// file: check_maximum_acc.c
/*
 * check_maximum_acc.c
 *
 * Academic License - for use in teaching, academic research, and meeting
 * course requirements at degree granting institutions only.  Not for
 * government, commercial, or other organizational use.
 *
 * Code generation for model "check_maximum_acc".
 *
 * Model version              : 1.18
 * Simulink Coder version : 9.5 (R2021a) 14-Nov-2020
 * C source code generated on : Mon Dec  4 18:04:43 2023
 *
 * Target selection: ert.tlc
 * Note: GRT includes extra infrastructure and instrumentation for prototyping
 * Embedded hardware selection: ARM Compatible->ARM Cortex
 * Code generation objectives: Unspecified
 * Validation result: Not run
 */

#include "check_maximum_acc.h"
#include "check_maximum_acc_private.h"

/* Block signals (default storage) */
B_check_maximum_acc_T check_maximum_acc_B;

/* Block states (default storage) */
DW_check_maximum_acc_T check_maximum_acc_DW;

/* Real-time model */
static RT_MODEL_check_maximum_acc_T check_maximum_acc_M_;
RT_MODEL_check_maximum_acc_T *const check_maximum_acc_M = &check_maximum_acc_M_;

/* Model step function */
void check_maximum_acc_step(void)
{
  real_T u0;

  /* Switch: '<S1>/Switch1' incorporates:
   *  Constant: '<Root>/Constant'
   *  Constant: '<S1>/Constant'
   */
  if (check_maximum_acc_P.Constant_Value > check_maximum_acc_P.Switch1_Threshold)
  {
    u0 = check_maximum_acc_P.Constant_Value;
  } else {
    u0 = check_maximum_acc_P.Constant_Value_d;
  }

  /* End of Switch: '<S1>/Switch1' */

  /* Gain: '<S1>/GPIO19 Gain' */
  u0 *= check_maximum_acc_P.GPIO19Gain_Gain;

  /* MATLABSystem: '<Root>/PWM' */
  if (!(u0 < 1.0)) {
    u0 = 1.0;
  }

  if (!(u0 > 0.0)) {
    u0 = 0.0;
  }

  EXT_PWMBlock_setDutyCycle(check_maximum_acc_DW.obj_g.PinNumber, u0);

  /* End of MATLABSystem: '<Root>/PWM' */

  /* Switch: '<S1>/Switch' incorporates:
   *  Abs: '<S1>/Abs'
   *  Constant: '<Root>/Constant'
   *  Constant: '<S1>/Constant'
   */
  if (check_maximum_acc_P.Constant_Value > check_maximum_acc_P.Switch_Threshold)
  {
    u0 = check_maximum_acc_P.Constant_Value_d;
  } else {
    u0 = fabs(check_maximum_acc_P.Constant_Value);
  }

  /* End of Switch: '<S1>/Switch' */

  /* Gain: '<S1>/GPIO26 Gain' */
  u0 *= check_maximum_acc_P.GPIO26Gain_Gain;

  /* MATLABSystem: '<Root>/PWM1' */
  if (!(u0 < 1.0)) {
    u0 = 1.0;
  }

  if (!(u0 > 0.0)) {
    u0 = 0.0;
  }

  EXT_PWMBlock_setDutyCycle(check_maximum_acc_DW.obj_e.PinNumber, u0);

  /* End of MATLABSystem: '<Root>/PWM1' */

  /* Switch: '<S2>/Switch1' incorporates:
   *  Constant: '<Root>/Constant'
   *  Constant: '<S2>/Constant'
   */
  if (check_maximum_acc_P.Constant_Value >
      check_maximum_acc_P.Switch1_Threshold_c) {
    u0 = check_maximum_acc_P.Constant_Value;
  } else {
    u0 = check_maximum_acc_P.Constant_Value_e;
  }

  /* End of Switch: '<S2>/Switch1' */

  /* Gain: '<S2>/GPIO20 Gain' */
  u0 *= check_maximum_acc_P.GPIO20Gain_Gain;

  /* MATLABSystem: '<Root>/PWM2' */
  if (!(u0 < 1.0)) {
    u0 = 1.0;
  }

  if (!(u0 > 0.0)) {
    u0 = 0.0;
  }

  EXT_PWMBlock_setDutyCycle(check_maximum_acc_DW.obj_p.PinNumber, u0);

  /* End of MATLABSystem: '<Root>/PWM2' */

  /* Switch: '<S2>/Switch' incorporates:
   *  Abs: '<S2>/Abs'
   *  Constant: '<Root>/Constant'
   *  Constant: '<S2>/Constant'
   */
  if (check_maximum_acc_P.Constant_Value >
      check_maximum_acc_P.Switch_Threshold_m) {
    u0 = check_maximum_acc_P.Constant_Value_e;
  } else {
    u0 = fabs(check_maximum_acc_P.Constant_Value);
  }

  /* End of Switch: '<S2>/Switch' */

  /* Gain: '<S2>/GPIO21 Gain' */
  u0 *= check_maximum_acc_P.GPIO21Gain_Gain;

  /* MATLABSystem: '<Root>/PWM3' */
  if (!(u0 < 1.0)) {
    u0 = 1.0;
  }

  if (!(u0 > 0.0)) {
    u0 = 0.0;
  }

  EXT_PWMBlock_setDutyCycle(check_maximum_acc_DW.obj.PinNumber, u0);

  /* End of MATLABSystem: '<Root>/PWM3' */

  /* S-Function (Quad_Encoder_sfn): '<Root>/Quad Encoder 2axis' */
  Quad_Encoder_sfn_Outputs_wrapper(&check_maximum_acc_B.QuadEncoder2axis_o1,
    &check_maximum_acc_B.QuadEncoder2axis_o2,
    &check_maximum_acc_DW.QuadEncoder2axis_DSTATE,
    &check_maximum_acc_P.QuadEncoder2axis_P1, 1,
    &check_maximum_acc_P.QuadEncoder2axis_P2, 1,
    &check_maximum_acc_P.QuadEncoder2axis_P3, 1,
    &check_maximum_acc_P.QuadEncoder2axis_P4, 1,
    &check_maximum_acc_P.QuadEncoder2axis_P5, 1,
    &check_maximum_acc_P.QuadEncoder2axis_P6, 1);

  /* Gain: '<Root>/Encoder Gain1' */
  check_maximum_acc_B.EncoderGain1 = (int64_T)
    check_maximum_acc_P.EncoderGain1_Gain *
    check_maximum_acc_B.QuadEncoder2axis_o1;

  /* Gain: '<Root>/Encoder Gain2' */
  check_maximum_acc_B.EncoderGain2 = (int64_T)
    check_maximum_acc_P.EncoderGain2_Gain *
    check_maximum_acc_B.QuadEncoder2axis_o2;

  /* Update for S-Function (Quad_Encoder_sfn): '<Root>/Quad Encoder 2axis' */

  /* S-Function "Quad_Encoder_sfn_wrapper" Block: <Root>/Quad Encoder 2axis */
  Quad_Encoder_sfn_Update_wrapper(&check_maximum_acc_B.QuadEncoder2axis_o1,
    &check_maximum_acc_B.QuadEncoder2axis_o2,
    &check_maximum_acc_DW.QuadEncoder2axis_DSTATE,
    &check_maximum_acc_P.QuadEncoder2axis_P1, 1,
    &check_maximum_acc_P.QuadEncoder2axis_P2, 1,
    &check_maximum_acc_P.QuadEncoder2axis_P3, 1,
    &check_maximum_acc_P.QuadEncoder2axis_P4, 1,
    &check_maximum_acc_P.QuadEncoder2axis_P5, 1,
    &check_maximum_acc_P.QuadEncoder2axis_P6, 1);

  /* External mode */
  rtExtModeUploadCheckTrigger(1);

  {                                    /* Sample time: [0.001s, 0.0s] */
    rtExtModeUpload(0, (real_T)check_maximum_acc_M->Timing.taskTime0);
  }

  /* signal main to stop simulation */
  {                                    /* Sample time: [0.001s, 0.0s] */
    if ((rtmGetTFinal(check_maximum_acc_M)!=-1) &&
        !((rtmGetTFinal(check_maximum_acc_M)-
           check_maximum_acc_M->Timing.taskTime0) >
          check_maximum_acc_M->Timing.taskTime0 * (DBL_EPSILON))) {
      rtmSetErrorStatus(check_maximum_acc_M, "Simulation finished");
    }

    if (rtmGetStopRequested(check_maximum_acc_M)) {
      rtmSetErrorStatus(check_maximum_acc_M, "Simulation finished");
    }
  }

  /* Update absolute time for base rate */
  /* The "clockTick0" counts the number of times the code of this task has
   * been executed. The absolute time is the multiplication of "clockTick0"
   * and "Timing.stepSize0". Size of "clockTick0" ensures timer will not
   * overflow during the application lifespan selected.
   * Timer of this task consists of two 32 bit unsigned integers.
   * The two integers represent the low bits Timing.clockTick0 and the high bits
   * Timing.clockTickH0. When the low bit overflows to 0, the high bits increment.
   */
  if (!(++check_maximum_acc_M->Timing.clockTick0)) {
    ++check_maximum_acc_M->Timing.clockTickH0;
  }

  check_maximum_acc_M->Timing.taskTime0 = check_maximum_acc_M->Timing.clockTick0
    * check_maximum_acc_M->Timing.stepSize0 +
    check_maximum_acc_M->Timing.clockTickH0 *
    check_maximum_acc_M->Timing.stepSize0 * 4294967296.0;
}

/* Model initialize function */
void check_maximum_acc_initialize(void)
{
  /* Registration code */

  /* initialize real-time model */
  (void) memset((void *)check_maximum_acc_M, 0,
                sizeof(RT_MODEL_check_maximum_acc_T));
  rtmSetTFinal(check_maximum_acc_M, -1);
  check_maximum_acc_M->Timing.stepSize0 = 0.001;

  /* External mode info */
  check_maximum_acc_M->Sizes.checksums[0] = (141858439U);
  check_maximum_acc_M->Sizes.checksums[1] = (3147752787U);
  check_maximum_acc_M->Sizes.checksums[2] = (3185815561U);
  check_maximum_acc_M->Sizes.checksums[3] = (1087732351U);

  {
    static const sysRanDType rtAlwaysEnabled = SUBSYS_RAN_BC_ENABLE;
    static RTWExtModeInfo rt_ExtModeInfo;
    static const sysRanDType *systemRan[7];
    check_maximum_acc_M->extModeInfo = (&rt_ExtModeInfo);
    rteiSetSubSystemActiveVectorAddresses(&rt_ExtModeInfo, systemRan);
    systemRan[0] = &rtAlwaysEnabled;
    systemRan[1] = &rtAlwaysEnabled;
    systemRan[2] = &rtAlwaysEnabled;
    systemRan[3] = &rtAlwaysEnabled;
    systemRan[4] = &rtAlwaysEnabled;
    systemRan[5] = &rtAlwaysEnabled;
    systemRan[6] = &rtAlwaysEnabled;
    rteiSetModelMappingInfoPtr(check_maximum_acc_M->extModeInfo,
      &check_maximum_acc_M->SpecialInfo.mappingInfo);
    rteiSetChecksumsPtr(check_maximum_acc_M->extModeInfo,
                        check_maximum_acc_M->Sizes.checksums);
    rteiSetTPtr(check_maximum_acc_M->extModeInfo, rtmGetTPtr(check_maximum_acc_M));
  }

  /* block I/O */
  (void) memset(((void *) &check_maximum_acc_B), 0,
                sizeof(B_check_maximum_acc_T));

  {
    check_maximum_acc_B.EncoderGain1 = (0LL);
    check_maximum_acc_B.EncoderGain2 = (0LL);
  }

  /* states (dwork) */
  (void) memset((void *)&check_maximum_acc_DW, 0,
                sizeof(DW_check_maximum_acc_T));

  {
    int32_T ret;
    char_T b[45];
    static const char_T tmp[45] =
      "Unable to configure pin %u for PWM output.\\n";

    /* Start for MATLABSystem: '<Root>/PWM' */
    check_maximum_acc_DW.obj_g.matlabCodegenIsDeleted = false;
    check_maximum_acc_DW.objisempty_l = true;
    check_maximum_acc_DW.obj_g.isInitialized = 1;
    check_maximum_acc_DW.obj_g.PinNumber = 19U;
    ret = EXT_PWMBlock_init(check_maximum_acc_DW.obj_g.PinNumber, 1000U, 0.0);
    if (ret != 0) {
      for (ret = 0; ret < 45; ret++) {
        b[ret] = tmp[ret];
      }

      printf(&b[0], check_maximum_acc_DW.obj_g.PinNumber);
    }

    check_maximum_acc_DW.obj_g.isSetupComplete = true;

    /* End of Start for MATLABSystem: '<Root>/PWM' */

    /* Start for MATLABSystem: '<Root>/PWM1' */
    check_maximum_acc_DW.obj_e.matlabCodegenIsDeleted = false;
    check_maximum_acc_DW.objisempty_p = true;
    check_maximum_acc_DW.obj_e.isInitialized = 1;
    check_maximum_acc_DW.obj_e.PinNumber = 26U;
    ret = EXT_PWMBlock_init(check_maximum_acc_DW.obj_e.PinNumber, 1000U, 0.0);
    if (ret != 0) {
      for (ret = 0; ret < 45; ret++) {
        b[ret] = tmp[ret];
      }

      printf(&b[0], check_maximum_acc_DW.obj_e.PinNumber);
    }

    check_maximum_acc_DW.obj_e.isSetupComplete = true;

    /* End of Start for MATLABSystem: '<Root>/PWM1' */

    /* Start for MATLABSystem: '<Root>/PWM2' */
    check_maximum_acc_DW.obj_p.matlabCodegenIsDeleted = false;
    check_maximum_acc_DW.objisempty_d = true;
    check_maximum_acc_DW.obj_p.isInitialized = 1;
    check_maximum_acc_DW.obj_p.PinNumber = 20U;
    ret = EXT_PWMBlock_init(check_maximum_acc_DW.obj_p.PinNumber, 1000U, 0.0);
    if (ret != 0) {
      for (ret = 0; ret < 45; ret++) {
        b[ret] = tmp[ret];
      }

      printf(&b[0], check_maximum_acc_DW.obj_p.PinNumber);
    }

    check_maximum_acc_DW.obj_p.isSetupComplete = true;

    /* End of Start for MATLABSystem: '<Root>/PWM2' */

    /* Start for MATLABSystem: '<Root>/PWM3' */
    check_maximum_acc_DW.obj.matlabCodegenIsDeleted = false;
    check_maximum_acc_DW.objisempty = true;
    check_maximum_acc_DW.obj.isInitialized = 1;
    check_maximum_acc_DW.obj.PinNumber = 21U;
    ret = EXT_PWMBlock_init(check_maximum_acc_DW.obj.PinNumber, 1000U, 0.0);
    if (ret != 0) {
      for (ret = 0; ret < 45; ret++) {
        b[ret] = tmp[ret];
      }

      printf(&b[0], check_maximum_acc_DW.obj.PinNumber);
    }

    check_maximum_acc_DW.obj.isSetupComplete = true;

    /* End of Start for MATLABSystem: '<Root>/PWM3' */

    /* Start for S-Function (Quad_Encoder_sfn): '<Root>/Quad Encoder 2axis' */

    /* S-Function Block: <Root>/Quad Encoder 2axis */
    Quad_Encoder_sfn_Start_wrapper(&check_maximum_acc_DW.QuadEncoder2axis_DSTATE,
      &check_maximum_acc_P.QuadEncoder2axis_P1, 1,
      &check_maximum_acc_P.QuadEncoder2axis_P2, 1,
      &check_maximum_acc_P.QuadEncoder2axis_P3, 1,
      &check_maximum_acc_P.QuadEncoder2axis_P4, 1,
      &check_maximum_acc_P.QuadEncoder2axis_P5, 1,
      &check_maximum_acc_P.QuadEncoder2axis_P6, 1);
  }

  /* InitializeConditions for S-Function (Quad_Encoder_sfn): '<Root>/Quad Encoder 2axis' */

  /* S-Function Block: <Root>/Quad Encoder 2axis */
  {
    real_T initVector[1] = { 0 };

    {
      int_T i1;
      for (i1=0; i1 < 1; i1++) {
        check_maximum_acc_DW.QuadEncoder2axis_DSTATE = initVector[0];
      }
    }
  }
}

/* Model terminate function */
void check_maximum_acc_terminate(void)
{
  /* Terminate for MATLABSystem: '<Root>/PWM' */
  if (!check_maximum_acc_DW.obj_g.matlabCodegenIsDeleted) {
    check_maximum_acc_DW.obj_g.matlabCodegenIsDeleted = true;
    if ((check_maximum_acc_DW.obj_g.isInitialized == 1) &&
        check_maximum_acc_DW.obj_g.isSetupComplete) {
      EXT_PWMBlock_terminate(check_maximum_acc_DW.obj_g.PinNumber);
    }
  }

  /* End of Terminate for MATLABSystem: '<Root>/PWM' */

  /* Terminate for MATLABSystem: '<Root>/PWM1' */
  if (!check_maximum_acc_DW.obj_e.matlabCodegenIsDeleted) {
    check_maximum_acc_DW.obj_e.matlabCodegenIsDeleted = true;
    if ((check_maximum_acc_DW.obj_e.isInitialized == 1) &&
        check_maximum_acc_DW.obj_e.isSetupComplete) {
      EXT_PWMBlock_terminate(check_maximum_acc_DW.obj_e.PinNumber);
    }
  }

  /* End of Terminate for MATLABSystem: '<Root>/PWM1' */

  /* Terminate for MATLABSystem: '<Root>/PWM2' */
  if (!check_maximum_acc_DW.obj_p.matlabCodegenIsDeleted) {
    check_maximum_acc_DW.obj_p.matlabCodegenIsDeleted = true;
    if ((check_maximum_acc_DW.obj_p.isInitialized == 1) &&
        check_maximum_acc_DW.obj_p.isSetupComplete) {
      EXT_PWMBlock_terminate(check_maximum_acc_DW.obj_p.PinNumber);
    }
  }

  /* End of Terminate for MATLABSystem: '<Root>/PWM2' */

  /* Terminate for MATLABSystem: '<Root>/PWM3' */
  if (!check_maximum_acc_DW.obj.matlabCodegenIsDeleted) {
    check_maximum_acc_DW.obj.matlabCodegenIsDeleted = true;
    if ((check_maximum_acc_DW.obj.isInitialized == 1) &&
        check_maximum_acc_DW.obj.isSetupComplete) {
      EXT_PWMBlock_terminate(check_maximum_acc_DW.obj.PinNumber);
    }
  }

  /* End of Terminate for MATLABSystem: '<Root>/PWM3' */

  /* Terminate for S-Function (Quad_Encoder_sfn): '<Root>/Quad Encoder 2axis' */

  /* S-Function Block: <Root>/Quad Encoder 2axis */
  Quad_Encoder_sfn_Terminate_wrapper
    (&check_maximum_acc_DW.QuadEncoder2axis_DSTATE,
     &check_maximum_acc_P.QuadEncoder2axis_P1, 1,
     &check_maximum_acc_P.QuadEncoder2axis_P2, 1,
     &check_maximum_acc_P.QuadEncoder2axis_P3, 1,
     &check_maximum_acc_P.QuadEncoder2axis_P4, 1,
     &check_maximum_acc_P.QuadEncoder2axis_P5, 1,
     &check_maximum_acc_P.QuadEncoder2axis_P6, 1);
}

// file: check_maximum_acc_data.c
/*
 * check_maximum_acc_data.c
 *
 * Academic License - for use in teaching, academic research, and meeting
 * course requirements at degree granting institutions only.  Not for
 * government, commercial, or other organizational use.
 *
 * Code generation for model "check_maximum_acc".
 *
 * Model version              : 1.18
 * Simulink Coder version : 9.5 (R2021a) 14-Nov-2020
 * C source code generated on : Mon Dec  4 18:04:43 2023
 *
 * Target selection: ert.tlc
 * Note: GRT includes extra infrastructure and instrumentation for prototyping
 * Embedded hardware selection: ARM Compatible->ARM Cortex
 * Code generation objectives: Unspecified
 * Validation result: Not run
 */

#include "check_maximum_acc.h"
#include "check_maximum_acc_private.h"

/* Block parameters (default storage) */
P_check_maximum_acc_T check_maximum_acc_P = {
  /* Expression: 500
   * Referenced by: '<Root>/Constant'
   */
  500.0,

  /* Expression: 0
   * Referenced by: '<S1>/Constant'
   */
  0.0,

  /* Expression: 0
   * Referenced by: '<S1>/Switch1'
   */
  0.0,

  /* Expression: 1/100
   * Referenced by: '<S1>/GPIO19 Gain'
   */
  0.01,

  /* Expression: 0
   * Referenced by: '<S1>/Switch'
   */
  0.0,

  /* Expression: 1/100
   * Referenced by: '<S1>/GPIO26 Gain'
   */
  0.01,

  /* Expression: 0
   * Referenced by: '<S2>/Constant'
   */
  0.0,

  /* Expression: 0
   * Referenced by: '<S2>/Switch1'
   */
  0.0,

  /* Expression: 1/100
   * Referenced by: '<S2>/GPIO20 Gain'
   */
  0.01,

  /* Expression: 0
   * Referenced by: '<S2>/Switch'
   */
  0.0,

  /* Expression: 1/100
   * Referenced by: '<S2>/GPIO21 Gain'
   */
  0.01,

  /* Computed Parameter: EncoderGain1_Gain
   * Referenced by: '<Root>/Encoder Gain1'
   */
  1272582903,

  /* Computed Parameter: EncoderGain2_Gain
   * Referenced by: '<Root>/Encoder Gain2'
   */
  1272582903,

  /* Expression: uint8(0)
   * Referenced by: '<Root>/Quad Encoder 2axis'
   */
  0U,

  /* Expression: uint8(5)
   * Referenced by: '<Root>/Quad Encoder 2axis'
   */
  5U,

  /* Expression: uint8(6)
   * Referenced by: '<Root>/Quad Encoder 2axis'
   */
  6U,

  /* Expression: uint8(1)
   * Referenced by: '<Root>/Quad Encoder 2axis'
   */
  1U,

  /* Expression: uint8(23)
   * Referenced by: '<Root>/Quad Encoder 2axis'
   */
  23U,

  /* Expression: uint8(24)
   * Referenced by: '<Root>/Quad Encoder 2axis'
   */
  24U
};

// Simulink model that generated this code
simulink model "check_maximum_acc"  (R2021a)
settings: Solver=FixedStepAuto  StartTime=0.0  StopTime=inf  FixedStep=0.001  RelTol=1e-3  EnableMultiTasking=on
StopFcn:
  | mypi=raspi();
  | writeDigitalPin(mypi,19,0);
  | writeDigitalPin(mypi,26,0);
  | writeDigitalPin(mypi,20,0);
  | writeDigitalPin(mypi,21,0);
  | clear mypi;
libraries: raspberrypiBasiclib x4

== system check_maximum_acc ==
  note: Encoder Position (To Workspace)
  Constant : Constant  Value=5
  Encoder Gain1 : Gain  Gain=1/216
  Encoder Gain2 : Gain  Gain=1/216
  Motor Subsystem : Subsystem
  Motor Subsystem1 : Subsystem
  PWM : raspberrypiBasiclib/PWM  board=Pi 4 Model B  Pin_=19  Frequency=1000  blockPlatform=Raspberry Pi
  PWM1 : raspberrypiBasiclib/PWM  board=Pi 4 Model B  Pin_=26  Frequency=1000  blockPlatform=Raspberry Pi
  PWM2 : raspberrypiBasiclib/PWM  board=Pi 4 Model B  Pin_=20  Frequency=1000  blockPlatform=Raspberry Pi
  PWM3 : raspberrypiBasiclib/PWM  board=Pi 4 Model B  Pin_=21  Frequency=1000  blockPlatform=Raspberry Pi
  Quad Encoder 2axis : S-Function  InitFcn=try, set_param(gcb,'FunctionName','Quad_Encoder_sfn'), end  FunctionName=Quad_Encoder_sfn  Parameters=uint8(0),uint8(5),uint8(6),uint8(1),uint8(23),uint8(24)  SFunctionModules=Quad_Encoder_sfn_wrapper  SFunctionDeploymentMode=off  EnableBusSupport=off  mask(S-Function Builder){}
      mask init:
      | val = [[.9  0.75 0.75 1 1 .9 .9 1]',[1 1 0.75 0.75 .9 .9 1 .9]'];try , sys = get_param(gcb,'SfunBuilderFcnName');if isempty(sys), sys = get_param(gcb,'FunctionName'); end,catch, sys = get_param(gcb,'FunctionName'); end
  To Workspace : ToWorkspace  VariableName=controled_position  SaveFormat=Structure With Time  SampleTime=0.001
  To Workspace1 : ToWorkspace  VariableName=simout  SaveFormat=Timeseries  SampleTime=-1
  To Workspace2 : ToWorkspace  VariableName=simout1  SaveFormat=Timeseries  SampleTime=-1
  wires:
  Quad Encoder 2axis/1 -> Encoder Gain1/1
  Quad Encoder 2axis/2 -> Encoder Gain2/1
  Motor Subsystem/1(Out1) -> PWM/1
  Motor Subsystem/2(Out2) -> PWM1/1
  Motor Subsystem1/2(Out2) -> PWM3/1
  Motor Subsystem1/1(Out1) -> PWM2/1
  Constant/1 -> Motor Subsystem1/1(In1), Motor Subsystem/1(In1)
  Encoder Gain1/1 -> To Workspace1/1
  Encoder Gain2/1 -> To Workspace2/1

== system check_maximum_acc/Motor Subsystem ==
  In1 : Inport
  Abs : Abs
  Constant : Constant  Value=0
  GPIO19 Gain : Gain  Gain=1/100
  GPIO26 Gain : Gain  Gain=1/100
  Switch : Switch  Criteria=u2 > Threshold
  Switch1 : Switch  Criteria=u2 > Threshold
  Out1 : Outport
  Out2 : Outport  Port=2
  wires:
  Switch/1 -> GPIO26 Gain/1
  Abs/1 -> Switch/3
  Switch1/1 -> GPIO19 Gain/1
  In1/1 -> Abs/1, Switch/2, Switch1/1, Switch1/2
  Constant/1 -> Switch/1, Switch1/3
  GPIO26 Gain/1 -> Out2/1
  GPIO19 Gain/1 -> Out1/1

== system check_maximum_acc/Motor Subsystem1 ==
  In1 : Inport
  Abs : Abs
  Constant : Constant  Value=0
  GPIO20 Gain : Gain  Gain=1/100
  GPIO21 Gain : Gain  Gain=1/100
  Switch : Switch  Criteria=u2 > Threshold
  Switch1 : Switch  Criteria=u2 > Threshold
  Out1 : Outport
  Out2 : Outport  Port=2
  wires:
  Switch/1 -> GPIO21 Gain/1
  Abs/1 -> Switch/3
  Switch1/1 -> GPIO20 Gain/1
  In1/1 -> Abs/1, Switch/2, Switch1/1, Switch1/2
  Constant/1 -> Switch/1, Switch1/3
  GPIO21 Gain/1 -> Out2/1
  GPIO20 Gain/1 -> Out1/1
